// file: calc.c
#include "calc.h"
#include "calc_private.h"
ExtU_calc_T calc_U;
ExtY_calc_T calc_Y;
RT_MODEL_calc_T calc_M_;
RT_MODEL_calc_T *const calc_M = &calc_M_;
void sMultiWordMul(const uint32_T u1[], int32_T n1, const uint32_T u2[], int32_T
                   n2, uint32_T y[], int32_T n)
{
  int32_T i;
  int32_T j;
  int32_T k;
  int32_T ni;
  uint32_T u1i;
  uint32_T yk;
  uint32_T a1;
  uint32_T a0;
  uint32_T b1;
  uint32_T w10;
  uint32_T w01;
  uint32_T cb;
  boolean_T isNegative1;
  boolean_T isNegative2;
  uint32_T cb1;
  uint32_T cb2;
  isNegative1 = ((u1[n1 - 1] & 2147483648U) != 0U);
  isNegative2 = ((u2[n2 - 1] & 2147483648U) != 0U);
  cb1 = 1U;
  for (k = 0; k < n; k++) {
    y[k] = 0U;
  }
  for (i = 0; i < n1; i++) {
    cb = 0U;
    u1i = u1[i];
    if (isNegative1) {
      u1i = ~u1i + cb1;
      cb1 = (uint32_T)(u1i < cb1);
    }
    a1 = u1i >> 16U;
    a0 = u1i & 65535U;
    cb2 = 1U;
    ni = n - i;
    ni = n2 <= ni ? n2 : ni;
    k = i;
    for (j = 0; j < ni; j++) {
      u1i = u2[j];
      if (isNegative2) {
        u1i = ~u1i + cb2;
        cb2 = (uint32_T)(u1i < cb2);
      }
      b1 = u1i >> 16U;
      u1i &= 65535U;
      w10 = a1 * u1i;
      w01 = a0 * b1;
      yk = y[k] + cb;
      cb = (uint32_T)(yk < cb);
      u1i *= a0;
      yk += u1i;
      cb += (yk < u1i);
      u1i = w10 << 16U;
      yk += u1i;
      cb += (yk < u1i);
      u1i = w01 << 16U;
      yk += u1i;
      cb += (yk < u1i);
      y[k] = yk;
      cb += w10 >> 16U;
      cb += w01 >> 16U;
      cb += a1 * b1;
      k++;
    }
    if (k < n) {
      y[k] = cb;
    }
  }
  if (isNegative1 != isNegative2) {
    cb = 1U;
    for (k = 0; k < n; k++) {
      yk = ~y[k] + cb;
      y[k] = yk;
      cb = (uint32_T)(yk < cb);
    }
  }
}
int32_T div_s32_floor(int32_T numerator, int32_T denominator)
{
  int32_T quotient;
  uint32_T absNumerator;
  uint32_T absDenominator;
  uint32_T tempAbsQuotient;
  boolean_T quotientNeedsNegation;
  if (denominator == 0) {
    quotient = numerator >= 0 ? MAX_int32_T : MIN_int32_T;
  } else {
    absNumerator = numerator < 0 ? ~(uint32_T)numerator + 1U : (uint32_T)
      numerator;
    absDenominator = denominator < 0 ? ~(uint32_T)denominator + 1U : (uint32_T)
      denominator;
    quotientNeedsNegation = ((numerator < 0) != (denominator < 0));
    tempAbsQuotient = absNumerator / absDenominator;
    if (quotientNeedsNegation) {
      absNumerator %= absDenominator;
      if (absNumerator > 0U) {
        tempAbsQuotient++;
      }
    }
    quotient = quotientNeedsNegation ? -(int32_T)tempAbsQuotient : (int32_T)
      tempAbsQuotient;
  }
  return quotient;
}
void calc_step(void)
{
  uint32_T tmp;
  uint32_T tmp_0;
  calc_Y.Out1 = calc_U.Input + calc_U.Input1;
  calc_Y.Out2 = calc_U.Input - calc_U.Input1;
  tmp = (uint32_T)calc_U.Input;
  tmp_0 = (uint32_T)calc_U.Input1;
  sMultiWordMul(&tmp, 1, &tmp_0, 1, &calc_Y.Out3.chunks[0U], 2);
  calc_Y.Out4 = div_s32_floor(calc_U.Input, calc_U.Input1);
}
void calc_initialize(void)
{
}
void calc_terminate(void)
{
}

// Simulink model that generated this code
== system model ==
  Input : Inport
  Input1 : Inport
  Out1 : Outport  <- 1: Sum#1
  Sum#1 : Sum  <- 1: Input, 2: Input1
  Out2 : Outport  <- 1: Sum#2
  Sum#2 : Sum  Inputs=+-  <- 1: Input, 2: Input1
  Out3 : Outport  <- 1: Product#1
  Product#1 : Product  <- 1: Input, 2: Input1
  Out4 : Outport  <- 1: Product#2
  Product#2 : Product  Inputs=*/  <- 1: Input, 2: Input1
